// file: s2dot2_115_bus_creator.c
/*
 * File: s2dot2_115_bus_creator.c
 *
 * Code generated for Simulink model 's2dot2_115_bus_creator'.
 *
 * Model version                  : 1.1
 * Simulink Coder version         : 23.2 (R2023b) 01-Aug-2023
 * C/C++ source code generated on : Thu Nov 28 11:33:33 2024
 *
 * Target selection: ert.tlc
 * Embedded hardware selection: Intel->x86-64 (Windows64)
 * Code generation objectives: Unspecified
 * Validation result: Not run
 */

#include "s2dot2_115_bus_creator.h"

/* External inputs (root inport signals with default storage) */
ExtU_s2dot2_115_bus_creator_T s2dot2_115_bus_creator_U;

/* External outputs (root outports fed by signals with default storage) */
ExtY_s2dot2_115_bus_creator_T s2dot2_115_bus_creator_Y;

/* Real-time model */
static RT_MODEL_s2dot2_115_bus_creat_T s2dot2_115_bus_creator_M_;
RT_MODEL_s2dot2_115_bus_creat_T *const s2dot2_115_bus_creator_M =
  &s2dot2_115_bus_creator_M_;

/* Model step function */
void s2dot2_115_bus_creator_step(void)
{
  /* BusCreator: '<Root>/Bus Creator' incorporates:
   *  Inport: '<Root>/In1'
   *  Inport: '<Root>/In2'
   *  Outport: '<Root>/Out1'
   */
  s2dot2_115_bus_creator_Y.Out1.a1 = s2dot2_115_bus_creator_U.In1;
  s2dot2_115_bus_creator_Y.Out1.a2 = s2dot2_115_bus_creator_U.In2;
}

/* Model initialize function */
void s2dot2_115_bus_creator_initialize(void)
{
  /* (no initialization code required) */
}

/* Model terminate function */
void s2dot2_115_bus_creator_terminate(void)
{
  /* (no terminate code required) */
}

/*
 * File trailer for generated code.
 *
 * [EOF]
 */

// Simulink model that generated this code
simulink model "s2dot2_115_bus_creator"  (R2023b)
settings: Solver=FixedStepAuto  StartTime=0.0  StopTime=10.0  FixedStep=0.01  RelTol=1e-3

== system s2dot2_115_bus_creator ==
  In1 : Inport
  In2 : Inport  Port=2
  Bus Creator : BusCreator  Inputs=2  OutDataTypeStr=Bus: a  NonVirtualBus=on
  Out1 : Outport
  wires:
  In1/1 -> Bus Creator/1
  In2/1 -> Bus Creator/2
  Bus Creator/1 -> Out1/1
